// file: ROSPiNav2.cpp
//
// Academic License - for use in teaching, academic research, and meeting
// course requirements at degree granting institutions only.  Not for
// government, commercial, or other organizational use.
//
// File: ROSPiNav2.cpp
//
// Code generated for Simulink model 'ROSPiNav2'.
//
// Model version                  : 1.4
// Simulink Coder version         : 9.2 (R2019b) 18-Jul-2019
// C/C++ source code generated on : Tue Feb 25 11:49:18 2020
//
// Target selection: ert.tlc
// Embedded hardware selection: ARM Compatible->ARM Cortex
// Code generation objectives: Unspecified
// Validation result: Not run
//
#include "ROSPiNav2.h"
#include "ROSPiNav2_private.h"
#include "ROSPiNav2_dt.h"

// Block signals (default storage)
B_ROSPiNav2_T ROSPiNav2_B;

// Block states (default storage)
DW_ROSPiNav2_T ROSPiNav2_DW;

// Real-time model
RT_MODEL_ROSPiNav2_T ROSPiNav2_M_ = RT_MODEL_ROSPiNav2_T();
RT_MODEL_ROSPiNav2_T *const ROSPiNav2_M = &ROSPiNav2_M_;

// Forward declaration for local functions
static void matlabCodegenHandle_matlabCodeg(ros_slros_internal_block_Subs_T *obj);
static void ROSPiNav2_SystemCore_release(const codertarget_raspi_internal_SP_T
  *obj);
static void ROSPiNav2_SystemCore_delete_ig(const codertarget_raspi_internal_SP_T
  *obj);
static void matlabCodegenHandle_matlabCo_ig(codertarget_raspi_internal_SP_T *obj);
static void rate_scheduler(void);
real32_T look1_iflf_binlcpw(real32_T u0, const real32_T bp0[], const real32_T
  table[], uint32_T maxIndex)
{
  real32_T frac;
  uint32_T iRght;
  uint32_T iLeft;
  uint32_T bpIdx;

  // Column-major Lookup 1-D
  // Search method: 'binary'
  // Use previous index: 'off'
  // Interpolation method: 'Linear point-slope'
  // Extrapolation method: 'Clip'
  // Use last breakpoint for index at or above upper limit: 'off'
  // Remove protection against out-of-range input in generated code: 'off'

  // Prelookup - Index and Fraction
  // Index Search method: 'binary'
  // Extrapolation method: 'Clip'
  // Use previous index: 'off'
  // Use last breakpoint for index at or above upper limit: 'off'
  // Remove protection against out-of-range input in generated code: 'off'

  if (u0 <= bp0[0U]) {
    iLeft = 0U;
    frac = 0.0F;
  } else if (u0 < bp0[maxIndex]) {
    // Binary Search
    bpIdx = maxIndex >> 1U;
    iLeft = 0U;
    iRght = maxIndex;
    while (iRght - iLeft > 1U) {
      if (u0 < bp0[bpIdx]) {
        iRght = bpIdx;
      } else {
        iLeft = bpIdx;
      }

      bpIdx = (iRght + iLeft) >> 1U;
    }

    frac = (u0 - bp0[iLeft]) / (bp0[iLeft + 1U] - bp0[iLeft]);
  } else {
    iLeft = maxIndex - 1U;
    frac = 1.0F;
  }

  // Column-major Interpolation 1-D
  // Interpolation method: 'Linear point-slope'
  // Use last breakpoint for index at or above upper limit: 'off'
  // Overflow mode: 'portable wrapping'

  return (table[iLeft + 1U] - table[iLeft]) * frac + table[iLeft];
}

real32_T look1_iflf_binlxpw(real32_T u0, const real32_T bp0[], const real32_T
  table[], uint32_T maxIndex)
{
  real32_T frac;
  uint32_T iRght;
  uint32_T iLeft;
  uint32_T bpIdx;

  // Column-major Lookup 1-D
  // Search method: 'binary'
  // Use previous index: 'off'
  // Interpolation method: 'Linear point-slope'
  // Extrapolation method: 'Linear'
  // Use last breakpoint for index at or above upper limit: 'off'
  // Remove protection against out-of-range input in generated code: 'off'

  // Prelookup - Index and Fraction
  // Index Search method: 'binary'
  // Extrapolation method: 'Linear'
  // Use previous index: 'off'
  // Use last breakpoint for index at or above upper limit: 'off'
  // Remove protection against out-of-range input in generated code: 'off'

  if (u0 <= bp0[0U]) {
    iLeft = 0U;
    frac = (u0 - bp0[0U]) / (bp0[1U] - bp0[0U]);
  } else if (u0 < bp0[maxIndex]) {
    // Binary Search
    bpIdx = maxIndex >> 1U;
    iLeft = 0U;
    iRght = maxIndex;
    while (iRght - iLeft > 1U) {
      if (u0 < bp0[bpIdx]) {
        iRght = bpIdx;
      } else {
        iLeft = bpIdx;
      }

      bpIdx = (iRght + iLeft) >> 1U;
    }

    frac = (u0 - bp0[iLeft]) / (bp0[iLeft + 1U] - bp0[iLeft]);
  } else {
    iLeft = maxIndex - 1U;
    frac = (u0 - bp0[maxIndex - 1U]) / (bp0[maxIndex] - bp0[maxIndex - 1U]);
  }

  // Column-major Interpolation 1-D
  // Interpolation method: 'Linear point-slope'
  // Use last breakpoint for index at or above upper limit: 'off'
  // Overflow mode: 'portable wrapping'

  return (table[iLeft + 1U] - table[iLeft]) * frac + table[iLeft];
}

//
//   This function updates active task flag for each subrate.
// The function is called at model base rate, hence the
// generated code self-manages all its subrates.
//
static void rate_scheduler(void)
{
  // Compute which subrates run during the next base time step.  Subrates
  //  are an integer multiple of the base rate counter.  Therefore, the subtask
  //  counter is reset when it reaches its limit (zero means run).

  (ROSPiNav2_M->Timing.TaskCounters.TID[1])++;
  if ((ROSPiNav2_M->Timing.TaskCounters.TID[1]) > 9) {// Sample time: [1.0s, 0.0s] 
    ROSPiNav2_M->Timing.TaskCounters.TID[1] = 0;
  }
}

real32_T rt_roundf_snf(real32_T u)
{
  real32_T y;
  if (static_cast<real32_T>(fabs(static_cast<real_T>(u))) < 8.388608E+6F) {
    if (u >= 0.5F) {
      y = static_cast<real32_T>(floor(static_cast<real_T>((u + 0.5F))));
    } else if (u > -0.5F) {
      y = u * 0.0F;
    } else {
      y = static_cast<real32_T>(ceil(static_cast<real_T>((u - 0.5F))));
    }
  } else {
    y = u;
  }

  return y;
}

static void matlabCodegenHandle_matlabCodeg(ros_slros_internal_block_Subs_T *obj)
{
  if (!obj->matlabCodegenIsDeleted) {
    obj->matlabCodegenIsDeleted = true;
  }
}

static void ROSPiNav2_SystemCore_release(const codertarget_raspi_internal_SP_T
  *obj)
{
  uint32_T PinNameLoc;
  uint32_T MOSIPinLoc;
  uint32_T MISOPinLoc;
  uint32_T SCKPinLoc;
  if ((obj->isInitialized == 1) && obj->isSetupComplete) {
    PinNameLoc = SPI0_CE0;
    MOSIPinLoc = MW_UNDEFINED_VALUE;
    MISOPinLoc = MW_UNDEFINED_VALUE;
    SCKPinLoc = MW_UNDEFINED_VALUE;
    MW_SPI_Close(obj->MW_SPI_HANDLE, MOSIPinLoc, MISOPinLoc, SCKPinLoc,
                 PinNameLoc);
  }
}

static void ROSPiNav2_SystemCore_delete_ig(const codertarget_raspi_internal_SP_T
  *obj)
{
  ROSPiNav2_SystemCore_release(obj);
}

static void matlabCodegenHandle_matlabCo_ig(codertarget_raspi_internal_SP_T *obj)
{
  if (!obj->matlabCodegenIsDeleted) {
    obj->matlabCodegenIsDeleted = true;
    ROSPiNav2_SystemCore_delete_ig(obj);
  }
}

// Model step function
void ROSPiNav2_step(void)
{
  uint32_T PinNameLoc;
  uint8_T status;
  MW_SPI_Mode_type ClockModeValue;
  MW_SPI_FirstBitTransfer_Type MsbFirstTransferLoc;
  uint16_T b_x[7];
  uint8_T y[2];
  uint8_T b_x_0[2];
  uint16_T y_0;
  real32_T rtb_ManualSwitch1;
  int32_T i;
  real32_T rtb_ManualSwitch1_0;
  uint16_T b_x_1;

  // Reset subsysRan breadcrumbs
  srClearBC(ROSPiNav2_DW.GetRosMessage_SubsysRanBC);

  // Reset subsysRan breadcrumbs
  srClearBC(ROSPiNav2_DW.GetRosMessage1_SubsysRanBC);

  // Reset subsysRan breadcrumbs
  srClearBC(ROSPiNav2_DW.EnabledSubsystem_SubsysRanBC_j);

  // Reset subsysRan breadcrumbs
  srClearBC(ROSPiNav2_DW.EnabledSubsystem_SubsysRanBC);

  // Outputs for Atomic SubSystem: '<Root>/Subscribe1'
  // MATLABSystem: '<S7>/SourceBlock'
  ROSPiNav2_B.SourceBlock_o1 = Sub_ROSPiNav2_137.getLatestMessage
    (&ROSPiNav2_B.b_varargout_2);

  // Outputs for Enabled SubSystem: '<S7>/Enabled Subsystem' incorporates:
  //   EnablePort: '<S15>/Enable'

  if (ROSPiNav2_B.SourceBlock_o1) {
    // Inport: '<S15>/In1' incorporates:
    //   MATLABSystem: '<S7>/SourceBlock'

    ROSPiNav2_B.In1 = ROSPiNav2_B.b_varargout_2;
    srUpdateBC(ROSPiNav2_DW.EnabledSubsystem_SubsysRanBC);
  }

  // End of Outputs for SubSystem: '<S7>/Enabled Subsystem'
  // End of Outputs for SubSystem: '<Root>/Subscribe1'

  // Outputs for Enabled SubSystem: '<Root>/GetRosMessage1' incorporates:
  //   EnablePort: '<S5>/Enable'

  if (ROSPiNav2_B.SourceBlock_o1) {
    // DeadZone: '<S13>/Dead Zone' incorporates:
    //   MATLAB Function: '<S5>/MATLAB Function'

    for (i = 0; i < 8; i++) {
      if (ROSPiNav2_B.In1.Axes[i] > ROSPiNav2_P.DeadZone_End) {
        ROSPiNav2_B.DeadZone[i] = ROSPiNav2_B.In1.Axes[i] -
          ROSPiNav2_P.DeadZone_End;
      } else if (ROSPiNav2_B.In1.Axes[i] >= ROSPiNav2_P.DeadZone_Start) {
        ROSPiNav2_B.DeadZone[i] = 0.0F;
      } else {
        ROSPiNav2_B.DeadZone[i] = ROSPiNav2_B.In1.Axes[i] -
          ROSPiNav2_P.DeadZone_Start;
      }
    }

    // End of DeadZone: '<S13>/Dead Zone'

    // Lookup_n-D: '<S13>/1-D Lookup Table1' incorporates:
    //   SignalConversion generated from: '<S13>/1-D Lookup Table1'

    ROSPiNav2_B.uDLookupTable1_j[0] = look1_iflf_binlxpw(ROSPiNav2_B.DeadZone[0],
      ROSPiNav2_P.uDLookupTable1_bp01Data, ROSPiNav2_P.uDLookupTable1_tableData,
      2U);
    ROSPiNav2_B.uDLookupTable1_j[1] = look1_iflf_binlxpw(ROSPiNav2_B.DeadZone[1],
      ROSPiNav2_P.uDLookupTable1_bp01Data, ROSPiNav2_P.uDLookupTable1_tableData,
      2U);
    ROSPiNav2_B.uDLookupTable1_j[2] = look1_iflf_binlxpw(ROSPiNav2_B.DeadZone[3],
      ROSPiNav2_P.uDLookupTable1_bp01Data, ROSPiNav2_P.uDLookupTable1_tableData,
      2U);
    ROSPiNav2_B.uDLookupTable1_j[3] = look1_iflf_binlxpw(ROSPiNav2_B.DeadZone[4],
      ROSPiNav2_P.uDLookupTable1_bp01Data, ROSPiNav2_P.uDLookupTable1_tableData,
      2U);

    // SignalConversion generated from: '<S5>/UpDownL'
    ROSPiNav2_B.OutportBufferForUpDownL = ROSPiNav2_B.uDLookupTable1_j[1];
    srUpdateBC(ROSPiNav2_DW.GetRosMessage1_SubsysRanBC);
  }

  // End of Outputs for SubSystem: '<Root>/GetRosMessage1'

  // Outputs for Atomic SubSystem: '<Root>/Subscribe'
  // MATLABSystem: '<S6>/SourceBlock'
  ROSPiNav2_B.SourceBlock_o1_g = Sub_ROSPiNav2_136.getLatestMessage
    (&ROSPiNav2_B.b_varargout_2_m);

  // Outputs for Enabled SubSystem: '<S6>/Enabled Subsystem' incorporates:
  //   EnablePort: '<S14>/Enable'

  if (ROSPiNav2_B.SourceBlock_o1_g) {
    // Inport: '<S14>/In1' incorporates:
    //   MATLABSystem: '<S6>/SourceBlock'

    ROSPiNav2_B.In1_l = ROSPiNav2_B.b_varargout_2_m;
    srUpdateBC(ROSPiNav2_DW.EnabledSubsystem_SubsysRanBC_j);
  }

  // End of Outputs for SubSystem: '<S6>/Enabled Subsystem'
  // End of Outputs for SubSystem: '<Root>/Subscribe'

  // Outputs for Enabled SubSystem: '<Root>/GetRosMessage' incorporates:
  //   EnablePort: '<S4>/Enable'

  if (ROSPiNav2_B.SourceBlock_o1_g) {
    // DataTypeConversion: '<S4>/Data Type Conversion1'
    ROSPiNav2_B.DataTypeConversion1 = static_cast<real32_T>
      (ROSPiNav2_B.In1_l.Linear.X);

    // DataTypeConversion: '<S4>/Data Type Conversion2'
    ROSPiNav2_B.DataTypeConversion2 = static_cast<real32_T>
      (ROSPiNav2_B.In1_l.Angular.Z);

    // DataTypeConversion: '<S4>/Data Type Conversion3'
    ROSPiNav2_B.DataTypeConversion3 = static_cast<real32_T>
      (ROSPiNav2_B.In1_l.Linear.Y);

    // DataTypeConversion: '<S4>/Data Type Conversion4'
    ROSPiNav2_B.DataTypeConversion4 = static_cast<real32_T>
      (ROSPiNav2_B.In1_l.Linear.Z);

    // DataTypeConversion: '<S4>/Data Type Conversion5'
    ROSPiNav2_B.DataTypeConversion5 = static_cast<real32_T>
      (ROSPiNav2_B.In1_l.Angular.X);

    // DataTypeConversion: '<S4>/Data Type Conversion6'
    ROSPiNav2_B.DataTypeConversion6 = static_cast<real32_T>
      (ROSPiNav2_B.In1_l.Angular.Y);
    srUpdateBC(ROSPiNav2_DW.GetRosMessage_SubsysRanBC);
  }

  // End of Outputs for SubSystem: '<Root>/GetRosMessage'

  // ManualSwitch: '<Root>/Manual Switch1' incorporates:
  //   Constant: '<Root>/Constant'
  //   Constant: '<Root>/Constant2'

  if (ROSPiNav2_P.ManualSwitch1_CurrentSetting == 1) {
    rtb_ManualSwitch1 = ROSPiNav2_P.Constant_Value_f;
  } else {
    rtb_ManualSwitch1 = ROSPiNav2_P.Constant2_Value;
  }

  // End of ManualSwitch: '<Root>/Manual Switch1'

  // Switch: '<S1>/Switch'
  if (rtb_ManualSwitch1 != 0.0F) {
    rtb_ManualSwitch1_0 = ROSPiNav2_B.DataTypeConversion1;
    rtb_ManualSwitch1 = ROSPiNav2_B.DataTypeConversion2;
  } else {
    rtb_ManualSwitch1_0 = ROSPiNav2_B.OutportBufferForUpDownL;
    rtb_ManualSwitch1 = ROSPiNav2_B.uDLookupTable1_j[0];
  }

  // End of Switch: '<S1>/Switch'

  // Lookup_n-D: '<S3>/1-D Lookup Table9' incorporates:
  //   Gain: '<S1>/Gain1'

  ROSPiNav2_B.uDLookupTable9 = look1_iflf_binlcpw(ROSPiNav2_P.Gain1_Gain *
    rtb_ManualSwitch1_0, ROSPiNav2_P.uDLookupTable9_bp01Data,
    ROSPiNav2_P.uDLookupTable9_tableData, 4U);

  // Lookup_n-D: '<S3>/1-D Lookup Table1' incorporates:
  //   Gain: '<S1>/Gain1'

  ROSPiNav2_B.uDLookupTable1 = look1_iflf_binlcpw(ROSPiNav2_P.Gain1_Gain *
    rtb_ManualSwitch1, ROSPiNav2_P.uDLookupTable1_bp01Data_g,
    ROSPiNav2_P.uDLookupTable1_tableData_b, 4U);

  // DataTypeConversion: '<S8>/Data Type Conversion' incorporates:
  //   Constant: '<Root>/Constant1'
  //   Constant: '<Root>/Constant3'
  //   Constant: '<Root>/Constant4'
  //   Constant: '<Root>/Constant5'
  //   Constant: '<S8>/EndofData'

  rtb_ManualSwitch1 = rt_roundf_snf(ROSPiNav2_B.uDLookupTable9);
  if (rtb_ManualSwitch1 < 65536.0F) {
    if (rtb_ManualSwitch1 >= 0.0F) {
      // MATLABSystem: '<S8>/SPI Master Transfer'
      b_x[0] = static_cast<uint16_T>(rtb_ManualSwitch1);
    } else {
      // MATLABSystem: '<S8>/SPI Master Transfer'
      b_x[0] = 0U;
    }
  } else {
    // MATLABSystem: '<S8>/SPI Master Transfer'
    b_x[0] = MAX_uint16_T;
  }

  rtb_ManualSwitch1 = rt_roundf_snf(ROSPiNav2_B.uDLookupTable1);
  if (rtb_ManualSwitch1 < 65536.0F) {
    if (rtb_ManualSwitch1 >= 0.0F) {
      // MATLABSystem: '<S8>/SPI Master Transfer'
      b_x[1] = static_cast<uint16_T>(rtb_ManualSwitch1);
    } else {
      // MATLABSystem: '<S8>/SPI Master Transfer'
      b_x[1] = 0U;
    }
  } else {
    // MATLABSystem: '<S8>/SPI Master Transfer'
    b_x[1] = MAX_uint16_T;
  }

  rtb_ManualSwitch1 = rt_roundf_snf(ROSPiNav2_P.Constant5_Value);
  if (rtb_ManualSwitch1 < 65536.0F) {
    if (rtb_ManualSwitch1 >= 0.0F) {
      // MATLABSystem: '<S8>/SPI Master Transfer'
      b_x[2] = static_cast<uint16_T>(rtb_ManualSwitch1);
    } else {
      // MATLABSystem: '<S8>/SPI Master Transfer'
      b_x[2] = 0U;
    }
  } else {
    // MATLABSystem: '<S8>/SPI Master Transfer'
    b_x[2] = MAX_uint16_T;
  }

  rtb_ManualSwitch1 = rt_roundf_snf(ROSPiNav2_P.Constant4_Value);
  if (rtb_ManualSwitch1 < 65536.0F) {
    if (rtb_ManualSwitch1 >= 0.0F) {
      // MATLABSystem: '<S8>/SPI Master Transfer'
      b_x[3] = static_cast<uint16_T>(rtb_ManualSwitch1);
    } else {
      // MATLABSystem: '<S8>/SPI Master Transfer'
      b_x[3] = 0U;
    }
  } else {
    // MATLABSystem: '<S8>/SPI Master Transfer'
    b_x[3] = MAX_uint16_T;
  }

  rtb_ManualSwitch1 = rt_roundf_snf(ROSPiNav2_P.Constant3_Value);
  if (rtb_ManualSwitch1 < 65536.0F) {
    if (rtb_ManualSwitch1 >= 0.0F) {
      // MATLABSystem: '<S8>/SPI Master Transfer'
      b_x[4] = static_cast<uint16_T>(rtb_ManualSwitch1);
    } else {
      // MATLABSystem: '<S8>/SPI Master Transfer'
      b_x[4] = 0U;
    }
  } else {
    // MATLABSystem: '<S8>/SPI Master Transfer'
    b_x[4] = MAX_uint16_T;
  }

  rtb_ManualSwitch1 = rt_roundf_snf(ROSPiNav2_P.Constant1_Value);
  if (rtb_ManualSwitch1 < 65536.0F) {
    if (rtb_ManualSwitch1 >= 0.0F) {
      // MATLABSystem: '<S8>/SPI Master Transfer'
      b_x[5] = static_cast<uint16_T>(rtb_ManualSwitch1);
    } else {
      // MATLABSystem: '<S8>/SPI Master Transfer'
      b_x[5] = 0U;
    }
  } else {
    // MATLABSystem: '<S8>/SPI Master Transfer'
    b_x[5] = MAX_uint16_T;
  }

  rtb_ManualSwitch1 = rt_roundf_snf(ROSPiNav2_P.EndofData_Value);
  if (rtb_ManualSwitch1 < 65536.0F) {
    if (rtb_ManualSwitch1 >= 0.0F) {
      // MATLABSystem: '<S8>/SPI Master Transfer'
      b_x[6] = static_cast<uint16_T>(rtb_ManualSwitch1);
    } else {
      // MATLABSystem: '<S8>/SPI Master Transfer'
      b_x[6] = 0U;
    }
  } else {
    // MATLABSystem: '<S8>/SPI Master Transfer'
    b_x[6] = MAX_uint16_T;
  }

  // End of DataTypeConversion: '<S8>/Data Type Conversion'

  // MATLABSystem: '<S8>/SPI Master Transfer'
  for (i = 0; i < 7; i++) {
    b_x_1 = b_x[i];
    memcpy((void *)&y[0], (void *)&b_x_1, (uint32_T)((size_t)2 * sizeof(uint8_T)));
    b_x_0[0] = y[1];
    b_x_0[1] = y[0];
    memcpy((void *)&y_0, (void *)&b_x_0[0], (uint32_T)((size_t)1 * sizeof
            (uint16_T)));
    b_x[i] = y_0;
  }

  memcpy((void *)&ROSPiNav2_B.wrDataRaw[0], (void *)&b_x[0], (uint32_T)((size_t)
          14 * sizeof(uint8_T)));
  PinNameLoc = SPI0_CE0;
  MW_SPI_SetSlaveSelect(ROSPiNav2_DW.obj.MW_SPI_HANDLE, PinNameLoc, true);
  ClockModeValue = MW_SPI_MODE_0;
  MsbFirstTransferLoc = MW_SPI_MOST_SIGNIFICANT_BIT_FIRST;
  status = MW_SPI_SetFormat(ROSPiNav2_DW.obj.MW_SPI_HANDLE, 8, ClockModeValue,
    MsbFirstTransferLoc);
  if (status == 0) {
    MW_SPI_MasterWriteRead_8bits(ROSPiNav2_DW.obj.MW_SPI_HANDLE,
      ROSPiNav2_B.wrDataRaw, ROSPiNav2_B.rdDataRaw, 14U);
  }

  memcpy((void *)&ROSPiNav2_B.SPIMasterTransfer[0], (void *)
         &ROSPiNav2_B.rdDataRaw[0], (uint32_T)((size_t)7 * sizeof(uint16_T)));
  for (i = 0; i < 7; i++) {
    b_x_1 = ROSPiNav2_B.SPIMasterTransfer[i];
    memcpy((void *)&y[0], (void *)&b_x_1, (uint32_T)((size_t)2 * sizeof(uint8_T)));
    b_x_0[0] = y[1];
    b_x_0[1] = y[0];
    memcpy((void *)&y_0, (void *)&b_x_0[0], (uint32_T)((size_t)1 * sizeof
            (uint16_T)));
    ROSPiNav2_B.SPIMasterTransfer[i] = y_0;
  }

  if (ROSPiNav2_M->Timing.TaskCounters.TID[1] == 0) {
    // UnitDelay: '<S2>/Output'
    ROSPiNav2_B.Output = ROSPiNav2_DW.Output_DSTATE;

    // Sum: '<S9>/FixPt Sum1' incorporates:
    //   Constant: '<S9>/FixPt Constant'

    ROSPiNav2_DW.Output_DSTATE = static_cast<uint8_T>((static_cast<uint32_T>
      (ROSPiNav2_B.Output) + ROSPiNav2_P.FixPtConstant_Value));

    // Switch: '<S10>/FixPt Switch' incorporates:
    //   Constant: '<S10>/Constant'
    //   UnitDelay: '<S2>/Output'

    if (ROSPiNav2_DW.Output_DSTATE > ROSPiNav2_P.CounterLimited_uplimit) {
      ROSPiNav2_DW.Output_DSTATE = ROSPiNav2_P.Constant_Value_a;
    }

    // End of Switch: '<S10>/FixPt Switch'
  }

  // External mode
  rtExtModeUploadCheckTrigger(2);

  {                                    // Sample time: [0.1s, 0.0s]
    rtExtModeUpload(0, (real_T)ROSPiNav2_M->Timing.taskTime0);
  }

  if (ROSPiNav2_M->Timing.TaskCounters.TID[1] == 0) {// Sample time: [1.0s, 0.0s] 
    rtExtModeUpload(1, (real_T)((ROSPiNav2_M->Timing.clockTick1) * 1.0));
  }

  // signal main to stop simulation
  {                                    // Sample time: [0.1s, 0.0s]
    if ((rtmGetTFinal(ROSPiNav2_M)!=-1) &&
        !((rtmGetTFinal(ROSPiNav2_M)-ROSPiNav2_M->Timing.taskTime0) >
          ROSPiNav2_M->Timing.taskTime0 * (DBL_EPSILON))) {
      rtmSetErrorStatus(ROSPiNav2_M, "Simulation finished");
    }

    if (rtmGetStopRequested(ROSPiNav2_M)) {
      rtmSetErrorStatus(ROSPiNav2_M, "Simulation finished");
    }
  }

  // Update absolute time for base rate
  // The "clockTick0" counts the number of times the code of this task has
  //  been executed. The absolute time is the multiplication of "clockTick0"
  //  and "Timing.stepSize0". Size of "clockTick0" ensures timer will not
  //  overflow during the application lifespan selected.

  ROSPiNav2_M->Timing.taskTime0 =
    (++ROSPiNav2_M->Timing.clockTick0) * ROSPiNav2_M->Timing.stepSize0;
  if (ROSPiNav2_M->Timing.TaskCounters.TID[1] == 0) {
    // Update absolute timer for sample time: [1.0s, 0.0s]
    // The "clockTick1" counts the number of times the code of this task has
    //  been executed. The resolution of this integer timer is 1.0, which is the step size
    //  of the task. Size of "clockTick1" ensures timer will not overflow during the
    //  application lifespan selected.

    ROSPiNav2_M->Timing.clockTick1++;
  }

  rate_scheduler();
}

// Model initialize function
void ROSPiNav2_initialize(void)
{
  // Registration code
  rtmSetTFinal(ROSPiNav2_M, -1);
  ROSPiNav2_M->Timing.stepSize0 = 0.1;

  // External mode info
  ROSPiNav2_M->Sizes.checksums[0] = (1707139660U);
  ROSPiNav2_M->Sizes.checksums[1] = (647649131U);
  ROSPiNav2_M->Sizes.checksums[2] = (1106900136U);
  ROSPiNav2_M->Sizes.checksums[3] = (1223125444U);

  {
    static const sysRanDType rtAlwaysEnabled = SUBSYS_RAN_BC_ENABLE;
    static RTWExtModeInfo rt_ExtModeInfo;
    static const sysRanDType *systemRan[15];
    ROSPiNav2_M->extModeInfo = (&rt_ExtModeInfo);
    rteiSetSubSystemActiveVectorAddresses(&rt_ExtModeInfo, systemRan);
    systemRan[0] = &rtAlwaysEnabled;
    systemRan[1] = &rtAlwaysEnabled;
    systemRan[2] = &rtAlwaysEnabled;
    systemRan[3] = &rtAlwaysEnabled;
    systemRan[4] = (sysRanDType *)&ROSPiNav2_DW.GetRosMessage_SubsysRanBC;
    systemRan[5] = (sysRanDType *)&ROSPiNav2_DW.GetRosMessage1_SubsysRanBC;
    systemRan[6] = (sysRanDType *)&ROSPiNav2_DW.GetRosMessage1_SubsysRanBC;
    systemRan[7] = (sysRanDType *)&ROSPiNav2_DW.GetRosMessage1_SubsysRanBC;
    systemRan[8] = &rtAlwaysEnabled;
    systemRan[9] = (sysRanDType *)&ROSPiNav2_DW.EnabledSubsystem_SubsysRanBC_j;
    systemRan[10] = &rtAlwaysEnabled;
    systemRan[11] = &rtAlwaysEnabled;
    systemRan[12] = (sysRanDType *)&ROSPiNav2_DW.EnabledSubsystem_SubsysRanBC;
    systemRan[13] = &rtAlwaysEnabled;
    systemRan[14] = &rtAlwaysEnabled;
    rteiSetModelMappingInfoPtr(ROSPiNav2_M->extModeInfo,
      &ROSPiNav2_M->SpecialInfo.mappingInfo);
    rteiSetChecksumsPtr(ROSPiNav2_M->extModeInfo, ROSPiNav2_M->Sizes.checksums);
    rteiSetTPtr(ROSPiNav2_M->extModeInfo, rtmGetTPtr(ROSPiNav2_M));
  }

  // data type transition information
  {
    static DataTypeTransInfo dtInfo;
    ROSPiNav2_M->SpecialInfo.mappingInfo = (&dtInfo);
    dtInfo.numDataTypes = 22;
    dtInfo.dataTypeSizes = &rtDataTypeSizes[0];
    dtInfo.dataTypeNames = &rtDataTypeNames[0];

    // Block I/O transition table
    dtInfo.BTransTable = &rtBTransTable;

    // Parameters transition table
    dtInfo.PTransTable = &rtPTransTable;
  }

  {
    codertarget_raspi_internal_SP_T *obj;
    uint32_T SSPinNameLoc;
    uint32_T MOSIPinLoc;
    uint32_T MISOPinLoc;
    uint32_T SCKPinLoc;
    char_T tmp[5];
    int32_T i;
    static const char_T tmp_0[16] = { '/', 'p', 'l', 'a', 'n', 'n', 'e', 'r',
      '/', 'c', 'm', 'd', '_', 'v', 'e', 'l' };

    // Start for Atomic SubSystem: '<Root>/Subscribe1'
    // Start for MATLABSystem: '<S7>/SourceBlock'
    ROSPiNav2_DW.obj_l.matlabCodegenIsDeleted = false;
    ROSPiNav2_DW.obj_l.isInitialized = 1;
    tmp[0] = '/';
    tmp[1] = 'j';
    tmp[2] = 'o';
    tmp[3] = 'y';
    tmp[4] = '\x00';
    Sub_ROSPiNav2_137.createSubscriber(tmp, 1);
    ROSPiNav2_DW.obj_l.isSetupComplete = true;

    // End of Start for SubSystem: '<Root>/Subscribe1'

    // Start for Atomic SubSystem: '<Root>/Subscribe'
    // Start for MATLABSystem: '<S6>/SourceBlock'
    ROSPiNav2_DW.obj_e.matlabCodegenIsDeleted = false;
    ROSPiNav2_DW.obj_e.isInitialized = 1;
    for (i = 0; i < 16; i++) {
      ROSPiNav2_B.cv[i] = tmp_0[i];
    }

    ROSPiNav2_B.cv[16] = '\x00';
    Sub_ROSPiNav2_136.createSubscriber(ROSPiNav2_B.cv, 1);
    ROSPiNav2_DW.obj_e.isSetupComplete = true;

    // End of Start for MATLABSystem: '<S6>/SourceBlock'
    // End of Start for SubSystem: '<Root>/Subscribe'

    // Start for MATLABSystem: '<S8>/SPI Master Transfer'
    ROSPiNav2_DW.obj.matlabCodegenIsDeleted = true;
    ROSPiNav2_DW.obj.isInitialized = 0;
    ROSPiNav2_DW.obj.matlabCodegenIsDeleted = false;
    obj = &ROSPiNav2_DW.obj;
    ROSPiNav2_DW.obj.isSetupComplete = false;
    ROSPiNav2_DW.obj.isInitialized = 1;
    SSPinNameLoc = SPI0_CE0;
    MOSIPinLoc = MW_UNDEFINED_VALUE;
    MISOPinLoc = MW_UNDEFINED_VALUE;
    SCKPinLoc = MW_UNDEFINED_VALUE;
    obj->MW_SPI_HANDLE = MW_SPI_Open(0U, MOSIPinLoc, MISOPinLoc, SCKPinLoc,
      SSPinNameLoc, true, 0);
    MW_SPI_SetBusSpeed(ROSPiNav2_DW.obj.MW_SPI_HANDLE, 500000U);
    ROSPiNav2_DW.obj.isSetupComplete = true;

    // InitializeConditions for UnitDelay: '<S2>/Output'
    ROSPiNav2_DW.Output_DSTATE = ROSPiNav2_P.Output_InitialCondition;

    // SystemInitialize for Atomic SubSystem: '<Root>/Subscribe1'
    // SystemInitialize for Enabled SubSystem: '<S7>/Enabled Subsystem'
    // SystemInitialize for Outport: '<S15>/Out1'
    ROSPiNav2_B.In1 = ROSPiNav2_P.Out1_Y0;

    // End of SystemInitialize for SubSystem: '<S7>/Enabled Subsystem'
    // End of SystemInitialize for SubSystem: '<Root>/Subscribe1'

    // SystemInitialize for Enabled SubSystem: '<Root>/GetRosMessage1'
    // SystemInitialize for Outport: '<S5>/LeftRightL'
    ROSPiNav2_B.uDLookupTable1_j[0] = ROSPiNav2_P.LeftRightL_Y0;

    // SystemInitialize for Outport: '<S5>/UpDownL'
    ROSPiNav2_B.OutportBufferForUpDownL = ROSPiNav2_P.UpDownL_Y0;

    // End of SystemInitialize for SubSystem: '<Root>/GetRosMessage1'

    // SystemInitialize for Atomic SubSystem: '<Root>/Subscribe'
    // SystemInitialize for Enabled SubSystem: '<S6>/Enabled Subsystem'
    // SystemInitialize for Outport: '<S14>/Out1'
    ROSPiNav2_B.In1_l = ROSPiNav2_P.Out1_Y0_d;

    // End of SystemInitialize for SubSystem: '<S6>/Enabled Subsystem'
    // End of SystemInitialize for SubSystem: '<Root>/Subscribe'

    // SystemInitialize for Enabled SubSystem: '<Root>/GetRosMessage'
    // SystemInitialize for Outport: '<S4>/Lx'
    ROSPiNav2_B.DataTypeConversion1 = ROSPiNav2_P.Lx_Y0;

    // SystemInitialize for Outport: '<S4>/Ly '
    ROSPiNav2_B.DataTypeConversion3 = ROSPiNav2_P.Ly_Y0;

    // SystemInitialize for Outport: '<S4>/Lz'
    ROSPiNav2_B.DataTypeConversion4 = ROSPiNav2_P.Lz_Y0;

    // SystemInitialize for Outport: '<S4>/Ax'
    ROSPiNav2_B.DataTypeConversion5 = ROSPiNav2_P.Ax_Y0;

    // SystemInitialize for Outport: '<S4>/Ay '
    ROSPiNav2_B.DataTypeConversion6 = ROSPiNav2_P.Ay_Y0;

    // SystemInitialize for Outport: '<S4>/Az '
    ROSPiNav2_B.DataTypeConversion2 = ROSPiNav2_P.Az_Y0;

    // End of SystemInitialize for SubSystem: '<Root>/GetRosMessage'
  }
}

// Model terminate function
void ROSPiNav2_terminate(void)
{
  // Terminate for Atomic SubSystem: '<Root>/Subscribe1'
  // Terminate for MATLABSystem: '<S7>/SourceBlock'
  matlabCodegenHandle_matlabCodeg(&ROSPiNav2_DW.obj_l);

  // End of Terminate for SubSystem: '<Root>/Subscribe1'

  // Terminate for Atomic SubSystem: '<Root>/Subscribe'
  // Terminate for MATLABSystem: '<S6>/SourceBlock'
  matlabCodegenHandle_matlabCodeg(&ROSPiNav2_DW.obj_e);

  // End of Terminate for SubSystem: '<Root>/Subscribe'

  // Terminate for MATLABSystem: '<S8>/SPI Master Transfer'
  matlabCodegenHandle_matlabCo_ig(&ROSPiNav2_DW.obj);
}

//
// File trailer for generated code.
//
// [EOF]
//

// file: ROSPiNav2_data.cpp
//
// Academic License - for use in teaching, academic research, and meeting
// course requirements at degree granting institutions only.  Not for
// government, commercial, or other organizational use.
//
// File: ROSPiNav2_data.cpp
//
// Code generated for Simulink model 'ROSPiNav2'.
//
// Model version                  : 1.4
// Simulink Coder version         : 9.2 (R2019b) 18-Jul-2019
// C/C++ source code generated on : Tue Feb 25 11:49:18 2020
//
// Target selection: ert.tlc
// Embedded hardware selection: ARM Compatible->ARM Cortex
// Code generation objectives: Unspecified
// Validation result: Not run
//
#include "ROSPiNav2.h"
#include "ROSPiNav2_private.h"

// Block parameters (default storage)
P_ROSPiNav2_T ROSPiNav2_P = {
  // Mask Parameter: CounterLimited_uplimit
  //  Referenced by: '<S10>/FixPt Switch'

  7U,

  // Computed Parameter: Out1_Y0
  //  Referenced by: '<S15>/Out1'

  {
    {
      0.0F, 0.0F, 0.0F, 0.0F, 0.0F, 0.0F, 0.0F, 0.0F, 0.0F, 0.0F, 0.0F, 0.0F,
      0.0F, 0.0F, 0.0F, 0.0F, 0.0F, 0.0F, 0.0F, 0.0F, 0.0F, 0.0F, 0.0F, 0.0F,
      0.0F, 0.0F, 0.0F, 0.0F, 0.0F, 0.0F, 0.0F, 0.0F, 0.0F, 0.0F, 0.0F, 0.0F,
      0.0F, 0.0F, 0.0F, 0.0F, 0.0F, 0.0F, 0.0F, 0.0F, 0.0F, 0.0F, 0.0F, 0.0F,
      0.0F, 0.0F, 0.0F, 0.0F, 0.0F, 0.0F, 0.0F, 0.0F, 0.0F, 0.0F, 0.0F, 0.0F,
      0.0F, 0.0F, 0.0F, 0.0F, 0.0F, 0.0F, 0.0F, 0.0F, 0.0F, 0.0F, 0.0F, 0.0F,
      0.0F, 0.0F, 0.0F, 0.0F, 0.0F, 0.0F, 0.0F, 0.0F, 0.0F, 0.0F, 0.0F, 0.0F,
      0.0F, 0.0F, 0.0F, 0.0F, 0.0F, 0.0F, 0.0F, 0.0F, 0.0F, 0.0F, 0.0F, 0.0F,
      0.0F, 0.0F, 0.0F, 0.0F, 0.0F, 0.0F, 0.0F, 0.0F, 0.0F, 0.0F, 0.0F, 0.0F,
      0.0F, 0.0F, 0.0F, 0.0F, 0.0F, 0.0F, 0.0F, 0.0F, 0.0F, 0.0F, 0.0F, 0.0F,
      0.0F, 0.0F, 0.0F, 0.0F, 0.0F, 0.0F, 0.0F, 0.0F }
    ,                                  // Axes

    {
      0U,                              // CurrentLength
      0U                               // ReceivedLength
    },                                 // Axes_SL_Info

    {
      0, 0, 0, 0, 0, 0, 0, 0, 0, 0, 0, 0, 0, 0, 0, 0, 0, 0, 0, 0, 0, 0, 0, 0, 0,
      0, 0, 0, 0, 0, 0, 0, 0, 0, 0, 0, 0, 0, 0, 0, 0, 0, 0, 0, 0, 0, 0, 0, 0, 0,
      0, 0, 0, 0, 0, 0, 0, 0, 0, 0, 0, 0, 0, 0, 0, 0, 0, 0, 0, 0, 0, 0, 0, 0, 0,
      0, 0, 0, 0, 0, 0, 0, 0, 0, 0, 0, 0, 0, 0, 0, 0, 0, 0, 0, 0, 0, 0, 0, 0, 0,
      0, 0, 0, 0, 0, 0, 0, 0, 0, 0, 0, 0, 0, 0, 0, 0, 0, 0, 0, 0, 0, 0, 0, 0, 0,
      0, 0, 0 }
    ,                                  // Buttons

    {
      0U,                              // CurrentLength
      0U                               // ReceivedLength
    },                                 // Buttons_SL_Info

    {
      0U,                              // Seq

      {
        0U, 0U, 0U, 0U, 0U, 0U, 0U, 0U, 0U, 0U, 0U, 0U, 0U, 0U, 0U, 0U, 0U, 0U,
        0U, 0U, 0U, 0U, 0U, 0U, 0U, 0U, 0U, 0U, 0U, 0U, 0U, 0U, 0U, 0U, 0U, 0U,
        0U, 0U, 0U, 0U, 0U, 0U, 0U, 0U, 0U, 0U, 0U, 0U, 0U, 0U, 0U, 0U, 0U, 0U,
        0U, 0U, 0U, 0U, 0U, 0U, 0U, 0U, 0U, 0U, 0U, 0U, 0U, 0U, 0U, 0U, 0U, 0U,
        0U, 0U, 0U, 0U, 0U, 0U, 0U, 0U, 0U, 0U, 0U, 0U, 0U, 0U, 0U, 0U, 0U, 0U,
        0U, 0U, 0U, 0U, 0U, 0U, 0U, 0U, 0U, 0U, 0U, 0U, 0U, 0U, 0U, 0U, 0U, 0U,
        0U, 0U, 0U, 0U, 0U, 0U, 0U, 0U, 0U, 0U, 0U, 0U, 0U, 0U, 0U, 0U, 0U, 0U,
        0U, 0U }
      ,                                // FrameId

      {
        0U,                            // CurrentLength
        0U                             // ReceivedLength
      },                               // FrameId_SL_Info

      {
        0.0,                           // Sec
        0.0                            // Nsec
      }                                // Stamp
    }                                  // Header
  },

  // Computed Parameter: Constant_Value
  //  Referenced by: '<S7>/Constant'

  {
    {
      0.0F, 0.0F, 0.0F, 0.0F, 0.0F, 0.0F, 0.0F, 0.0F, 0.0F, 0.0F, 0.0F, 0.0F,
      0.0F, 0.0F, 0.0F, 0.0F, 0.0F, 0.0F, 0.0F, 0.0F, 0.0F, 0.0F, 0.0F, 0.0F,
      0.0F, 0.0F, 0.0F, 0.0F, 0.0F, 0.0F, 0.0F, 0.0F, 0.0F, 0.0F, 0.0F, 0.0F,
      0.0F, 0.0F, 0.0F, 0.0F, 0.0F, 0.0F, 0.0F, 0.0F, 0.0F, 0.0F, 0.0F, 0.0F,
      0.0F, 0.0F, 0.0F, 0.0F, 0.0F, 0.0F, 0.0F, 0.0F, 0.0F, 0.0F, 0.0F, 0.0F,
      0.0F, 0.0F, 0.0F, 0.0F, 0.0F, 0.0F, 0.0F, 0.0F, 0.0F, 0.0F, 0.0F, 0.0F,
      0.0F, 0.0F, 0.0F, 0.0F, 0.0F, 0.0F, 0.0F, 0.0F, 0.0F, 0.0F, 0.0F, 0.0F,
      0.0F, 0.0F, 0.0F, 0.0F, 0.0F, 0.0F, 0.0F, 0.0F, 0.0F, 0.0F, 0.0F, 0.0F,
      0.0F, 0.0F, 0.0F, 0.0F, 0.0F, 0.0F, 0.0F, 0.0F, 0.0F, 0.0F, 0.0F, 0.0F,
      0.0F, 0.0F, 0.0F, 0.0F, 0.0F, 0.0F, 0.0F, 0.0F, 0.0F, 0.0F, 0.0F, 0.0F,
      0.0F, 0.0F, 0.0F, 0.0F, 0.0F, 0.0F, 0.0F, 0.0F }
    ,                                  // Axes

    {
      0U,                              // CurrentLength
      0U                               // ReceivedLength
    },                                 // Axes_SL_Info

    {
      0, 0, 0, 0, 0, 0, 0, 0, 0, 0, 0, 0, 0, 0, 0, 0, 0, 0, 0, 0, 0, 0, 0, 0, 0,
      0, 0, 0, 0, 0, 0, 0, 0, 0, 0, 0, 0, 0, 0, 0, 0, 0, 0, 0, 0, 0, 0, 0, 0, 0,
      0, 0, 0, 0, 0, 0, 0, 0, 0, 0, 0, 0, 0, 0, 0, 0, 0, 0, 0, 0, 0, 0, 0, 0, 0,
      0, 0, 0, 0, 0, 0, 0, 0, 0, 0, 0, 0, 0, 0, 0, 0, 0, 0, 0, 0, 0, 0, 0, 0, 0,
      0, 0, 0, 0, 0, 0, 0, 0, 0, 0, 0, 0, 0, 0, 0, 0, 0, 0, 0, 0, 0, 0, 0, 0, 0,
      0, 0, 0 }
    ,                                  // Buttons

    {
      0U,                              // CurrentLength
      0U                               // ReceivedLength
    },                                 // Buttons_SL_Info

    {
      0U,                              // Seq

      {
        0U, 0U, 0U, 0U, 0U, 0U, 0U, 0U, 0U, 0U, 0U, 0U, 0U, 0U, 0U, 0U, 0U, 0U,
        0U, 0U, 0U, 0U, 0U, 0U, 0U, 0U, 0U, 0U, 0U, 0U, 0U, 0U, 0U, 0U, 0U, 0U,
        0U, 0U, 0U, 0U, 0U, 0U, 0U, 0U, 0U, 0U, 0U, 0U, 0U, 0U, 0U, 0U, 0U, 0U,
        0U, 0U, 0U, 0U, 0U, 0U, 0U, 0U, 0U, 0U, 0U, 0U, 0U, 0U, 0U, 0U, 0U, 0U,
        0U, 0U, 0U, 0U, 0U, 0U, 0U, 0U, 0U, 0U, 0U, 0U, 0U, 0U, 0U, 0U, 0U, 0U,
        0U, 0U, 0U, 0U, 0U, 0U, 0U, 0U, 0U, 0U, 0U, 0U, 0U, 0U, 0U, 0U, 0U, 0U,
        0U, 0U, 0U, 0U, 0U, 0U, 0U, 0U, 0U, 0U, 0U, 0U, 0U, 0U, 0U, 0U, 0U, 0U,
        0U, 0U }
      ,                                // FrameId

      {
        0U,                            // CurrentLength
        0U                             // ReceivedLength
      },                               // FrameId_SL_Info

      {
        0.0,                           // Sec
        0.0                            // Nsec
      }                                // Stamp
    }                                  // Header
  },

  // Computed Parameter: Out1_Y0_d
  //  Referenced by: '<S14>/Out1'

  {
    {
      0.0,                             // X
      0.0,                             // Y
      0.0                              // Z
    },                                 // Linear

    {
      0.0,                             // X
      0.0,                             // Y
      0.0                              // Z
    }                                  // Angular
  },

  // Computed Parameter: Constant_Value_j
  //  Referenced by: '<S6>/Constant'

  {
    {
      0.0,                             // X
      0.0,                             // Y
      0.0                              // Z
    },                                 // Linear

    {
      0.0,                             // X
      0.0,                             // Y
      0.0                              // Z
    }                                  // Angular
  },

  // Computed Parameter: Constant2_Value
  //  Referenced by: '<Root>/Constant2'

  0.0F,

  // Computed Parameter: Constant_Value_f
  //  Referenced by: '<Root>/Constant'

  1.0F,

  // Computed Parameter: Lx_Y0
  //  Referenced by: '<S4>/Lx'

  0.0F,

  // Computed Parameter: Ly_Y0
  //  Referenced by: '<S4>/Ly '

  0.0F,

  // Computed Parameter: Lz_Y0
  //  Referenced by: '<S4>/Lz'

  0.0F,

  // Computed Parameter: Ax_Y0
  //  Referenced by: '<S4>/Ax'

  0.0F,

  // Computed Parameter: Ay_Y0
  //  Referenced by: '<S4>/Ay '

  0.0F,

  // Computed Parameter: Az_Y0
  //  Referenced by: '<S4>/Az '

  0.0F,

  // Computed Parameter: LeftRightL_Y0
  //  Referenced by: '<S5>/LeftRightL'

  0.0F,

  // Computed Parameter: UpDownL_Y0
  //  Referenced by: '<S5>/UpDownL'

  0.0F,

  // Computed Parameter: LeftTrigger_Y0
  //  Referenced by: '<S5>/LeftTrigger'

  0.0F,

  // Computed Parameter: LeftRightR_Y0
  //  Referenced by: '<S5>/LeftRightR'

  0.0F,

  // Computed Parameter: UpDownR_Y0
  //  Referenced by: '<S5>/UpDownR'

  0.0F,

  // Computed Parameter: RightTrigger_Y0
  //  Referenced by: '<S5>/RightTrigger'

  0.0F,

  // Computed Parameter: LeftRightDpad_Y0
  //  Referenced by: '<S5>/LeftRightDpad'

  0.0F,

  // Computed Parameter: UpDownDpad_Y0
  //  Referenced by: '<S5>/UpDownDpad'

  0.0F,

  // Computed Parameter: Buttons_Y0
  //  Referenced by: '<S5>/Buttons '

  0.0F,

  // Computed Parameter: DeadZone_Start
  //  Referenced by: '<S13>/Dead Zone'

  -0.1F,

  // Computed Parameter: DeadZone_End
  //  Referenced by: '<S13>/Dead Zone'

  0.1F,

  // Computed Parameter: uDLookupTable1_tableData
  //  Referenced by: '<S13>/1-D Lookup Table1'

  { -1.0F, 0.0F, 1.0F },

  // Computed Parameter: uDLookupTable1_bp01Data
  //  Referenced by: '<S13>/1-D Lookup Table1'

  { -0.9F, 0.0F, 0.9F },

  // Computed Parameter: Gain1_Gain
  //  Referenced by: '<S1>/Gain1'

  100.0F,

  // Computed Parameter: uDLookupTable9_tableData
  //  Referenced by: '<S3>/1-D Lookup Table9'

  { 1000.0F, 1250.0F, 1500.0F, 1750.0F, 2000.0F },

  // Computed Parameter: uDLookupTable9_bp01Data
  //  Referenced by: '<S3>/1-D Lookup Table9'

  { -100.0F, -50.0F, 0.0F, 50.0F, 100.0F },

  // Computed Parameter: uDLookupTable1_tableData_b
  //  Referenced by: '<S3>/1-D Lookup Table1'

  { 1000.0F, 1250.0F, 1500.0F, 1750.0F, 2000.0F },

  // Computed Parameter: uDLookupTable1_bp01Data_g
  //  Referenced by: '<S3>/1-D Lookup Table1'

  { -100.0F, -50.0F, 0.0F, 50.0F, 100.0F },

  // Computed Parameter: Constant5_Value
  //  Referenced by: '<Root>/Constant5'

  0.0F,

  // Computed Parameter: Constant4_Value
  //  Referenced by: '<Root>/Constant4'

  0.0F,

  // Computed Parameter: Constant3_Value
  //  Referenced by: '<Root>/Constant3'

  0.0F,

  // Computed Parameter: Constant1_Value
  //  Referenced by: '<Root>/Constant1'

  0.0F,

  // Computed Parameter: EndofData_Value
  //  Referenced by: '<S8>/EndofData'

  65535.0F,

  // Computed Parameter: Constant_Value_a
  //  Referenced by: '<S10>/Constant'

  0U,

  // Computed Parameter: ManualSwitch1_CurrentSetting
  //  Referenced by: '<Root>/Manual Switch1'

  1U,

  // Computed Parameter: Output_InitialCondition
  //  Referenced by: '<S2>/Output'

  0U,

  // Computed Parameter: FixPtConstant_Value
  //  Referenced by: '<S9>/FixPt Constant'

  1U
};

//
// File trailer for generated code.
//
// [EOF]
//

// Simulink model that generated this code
simulink model "ROSPiNav2"  (Simulink 10.0)
settings: Solver=FixedStepAuto  StartTime=0.0  StopTime=inf  RelTol=1e-3
libraries: sensehatlib x5, robotlib x2, simulink x1, raspberrypilib x1

== system ROSPiNav2 ==
  note: Arbitration
  note: Xbox Controller
  note: Raspbery Pi Sense Hat
  note: Switch Xbox or AutoNav
  note: Cheeky Dev Interface
  note: Xbox
  note: Counter to show Pi is functiuoning when running in external mode
  note: Send Data
  note: Navigation Stack
  note: Mapping
  note: AutoNav
  Arbitration : Subsystem
  Constant : Constant  OutDataTypeStr=single
  Constant{1..5} (5 alike) : Constant  Value=0  OutDataTypeStr=single
  Constant6 : Constant  Commented=on  Value=0  OutDataTypeStr=single
  Constant7 : Constant  Commented=on  Value=0  OutDataTypeStr=single
  Counter Limited : simulink/Sources/Counter Limited  uplimit=7  tsamp=1
  Display{1..6,15} (7 alike) : Display
  ForwardBack_LeftRight : Subsystem
  From2 : From  Commented=on  GotoTag=SenseHatOut
  GetRosMessage : Subsystem
  GetRosMessage1 : Subsystem
  Goto2 : Goto  Commented=on  GotoTag=SenseHatOut
  Manual Switch1 : ManualSwitch
  Mux : Mux  Commented=on  Inputs=7
  Mux1 : Mux  Inputs=2
  Mux2 : Mux  Inputs=6
  Mux3 : Mux  Inputs=2
  PiSenseHat : Subsystem  Commented=on
  SPI Return : Display
  Subscribe : robotlib/Subscribe  topicSource=Select from ROS network  topic=/planner/cmd_vel  messageType=geometry_msgs/Twist  sampleTime=0.1  messageQueueLength=1
  Subscribe1 : robotlib/Subscribe  topicSource=Specify your own  topic=/joy  messageType=sensor_msgs/Joy  sampleTime=0.1  messageQueueLength=1
  Subsystem : Subsystem
  Terminator{1..11} (11 alike) : Terminator
  wires:
  GetRosMessage1/2(UpDownL) -> Mux1/2, Arbitration/3("ControllerUpDown ")
  [SPIOutput] -> SPI Return/1
  Mux3/1 -> [DataSent]
  [DataSent] -> Display6/1
  [InputCmd] -> Arbitration/5("Switch ")
  GetRosMessage1/9("Buttons ") -> Terminator11/1
  Constant5/1 -> Subsystem/3(Spare1)
  GetRosMessage1/7(LeftRightDpad) -> Terminator9/1
  Constant4/1 -> Subsystem/4(Spare2)
  Constant/1 -> Manual Switch1/1
  ForwardBack_LeftRight/1(ForwardsBack) -> Mux3/1, Subsystem/1(ForwardsBackwards)
  ForwardBack_LeftRight/2(LeftRight) -> Mux3/2, Subsystem/2(LeftRight)
  GetRosMessage1/5(UpDownR) -> Terminator7/1
  Arbitration/1(ForwardBackOut) -> ForwardBack_LeftRight/1(In1)
  Subscribe/2 -> GetRosMessage/1(In1)
  GetRosMessage/5("Ay ") -> Mux2/5, Terminator5/1
  GetRosMessage/3(Lz) -> Mux2/3, Terminator3/1
  Constant2/1 -> Manual Switch1/2
  GetRosMessage/4(Ax) -> Mux2/4, Terminator4/1
  GetRosMessage1/4(LeftRightR) -> Terminator6/1
  PiSenseHat/1(PressureP) -> Mux/1
  From2/1 -> Display3/1
  Subscribe/1 -> GetRosMessage/Enable, Display1/1
  GetRosMessage/2("Ly ") -> Mux2/2, Terminator2/1
  Subscribe1/2 -> GetRosMessage1/1(In1)
  [XboxOut] -> Display5/1
  PiSenseHat/7(HumidityT) -> Mux/7
  Constant3/1 -> Subsystem/5(Spare3)
  GetRosMessage1/8(UpDownDpad) -> Terminator10/1
  Mux2/1 -> [NavStackOut]
  Subscribe1/1 -> GetRosMessage1/Enable, Display2/1
  GetRosMessage/6("Az ") -> Arbitration/2(LeftyRightyIn), Mux2/6  "Left_right"
  PiSenseHat/5(MagField) -> Mux/5
  Subsystem/1(SpiData) -> [SPIOutput]
  Constant1/1 -> Subsystem/6(Spare4)
  Mux1/1 -> [XboxOut]
  PiSenseHat/4(Accel) -> Mux/4
  Counter Limited/1 -> Display15/1
  GetRosMessage1/1(LeftRightL) -> Mux1/1, Arbitration/4(ControllerLeftRight)
  GetRosMessage1/3(LeftTrigger) -> Terminator1/1
  GetRosMessage1/6(RightTrigger) -> Terminator8/1
  Arbitration/2(LeftyRightyOut) -> ForwardBack_LeftRight/2(In2)
  GetRosMessage/1(Lx) -> Mux2/1, Arbitration/1(ForwardBackIn)  "Forward_Back"
  [NavStackOut] -> Display4/1
  Manual Switch1/1 -> [InputCmd]
  PiSenseHat/3(AngVelocity) -> Mux/3
  Mux/1 -> Goto2/1
  PiSenseHat/6(HumidityH) -> Mux/6
  PiSenseHat/2(PressureT) -> Mux/2

== system ROSPiNav2/Arbitration ==
  note: Possibility here to switch from the commands to a fixed velocity
  note: Looking here to see if we are on the stright and narrow if not, pause and rotate before moving forwards.
      | The data coming from the Navigation node gives forward velocity and twist velocity. this ranges from -0.5 to 0.5 on both sides.
  ForwardBackIn : Inport
  LeftyRightyIn : Inport  Port=2
  "ControllerUpDown " : Inport  Port=3
  ControllerLeftRight : Inport  Port=4
  "Switch " : Inport  Port=5
  Demux : Demux  Outputs=2
  Gain1 : Gain  Gain=100
  Mux1 : Mux  Inputs=2
  Mux2 : Mux  Inputs=2
  Switch : Switch  Criteria=u2 ~= 0
  ForwardBackOut : Outport
  LeftyRightyOut : Outport  Port=2
  wires:
  LeftyRightyIn/1 -> Mux2/2
  Demux/1 -> ForwardBackOut/1
  Demux/2 -> LeftyRightyOut/1
  Switch/1 -> Gain1/1
  "ControllerUpDown "/1 -> Mux1/1
  ControllerLeftRight/1 -> Mux1/2
  Mux1/1 -> Switch/3
  "Switch "/1 -> Switch/2
  Gain1/1 -> Demux/1
  Mux2/1 -> Switch/1
  ForwardBackIn/1 -> Mux2/1

== system ROSPiNav2/ForwardBack_LeftRight ==
  note: input a -100 to 100 value for reverse and forwards. -100 is 100% speed backwards 100 is 100%speed forwards
  note: input a -100 to 100 value for left and right. -100 is 100% speed left 100 is 100%speed right
  In1 : Inport
  In2 : Inport  Port=2
  1-D Lookup Table1 : Lookup_n-D  NumberOfTableDimensions=1  BreakpointsForDimension1=[-100,-50,0,50,100]  BreakpointsForDimension1FirstPoint=0  BreakpointsForDimension1Spacing=1.8  Table=[1000;1250;1500;1750;2000;]  ExtrapMethod=Clip  InternalRulePriority=Speed  OutDataTypeStr=single  RndMeth=Simplest  InputSameDT=on
  1-D Lookup Table9 : Lookup_n-D  NumberOfTableDimensions=1  BreakpointsForDimension1=[-100,-50,0,50,100]  BreakpointsForDimension1FirstPoint=0  BreakpointsForDimension1Spacing=1.8  Table=[1000;1250;1500;1750;2000]  ExtrapMethod=Clip  InternalRulePriority=Speed  OutDataTypeStr=single  RndMeth=Simplest  InputSameDT=on
  ForwardsBack : Outport  OutDataTypeStr=single
  LeftRight : Outport  Port=2  OutDataTypeStr=single
  wires:
  In1/1 -> 1-D Lookup Table9/1
  1-D Lookup Table1/1 -> LeftRight/1
  1-D Lookup Table9/1 -> ForwardsBack/1
  In2/1 -> 1-D Lookup Table1/1

== system ROSPiNav2/GetRosMessage ==
  note: Linear Commands
  note: AngularCommands
  In1 : Inport
  Enable : EnablePort
  Bus Selector : BusSelector  OutputSignals=Linear.X,Linear.Y,Linear.Z,Angular.X,Angular.Y,Angular.Z
  Data Type Conversion{1..6} (6 alike) : DataTypeConversion  OutDataTypeStr=single
  Lx : Outport  OutDataTypeStr=single
  "Ly " : Outport  Port=2
  Lz : Outport  Port=3
  Ax : Outport  Port=4
  "Ay " : Outport  Port=5
  "Az " : Outport  Port=6  OutDataTypeStr=single
  wires:
  Bus Selector/2 -> Data Type Conversion3/1  "<Y>"
  Bus Selector/1 -> Data Type Conversion1/1  "<X>"
  In1/1 -> Bus Selector/1
  Bus Selector/3 -> Data Type Conversion4/1  "<Z>"
  Bus Selector/4 -> Data Type Conversion5/1  "<X>"
  Bus Selector/5 -> Data Type Conversion6/1  "<Y>"
  Bus Selector/6 -> Data Type Conversion2/1  "<Z>"
  Data Type Conversion1/1 -> Lx/1
  Data Type Conversion2/1 -> "Az "/1
  Data Type Conversion3/1 -> "Ly "/1
  Data Type Conversion4/1 -> Lz/1
  Data Type Conversion5/1 -> Ax/1
  Data Type Conversion6/1 -> "Ay "/1

== system ROSPiNav2/GetRosMessage1 ==
  note: Axes
  In1 : Inport
  Enable : EnablePort
  Bus Selector : BusSelector  OutputSignals=Axes,Buttons
  Data Type Conversion1 : DataTypeConversion  OutDataTypeStr=single
  Data Type Conversion3 : DataTypeConversion  OutDataTypeStr=single
  Demux : Demux  Outputs=8
  MATLAB Function : MATLAB Function  TreatAsAtomicUnit=on
  MATLAB Function1 : MATLAB Function  TreatAsAtomicUnit=on
  "XboxControllerMappings " : Subsystem
  LeftRightL : Outport  OutDataTypeStr=single
  UpDownL : Outport  Port=2  OutDataTypeStr=single
  LeftTrigger : Outport  Port=3  OutDataTypeStr=single
  LeftRightR : Outport  Port=4  OutDataTypeStr=single
  UpDownR : Outport  Port=5  OutDataTypeStr=single
  RightTrigger : Outport  Port=6  OutDataTypeStr=single
  LeftRightDpad : Outport  Port=7  OutDataTypeStr=single
  UpDownDpad : Outport  Port=8  OutDataTypeStr=single
  "Buttons " : Outport  Port=9
  wires:
  Data Type Conversion3/1 -> "Buttons "/1
  Demux/1 -> LeftRightL/1
  In1/1 -> Bus Selector/1
  Bus Selector/1 -> MATLAB Function/1(in)  "<Axes>"
  Bus Selector/2 -> MATLAB Function1/1(in)  "<Buttons>"
  Data Type Conversion1/1 -> "XboxControllerMappings "/1(Axisin)
  Demux/2 -> UpDownL/1
  Demux/3 -> LeftTrigger/1
  Demux/4 -> LeftRightR/1
  Demux/5 -> UpDownR/1
  Demux/6 -> RightTrigger/1
  Demux/7 -> LeftRightDpad/1
  "XboxControllerMappings "/1(AxisOut) -> Demux/1
  Demux/8 -> UpDownDpad/1
  MATLAB Function/1(out) -> Data Type Conversion1/1
  MATLAB Function1/1(out) -> Data Type Conversion3/1

== system ROSPiNav2/PiSenseHat ==
  note: For some reason the GPIO is broken. I don't know why. but these two blocks do not work. However the IMU data we care about is fine
  "8x8 RGB LED Matrix " : sensehatlib/8x8 RGB LED Matrix   Commented=on  Mode=Write Pixel  ImageSource=One multidimensional signal  OrientationSource=Block dialog  LEDOrientation=0  blockPlatform=Raspberry pi
  Display3 : Display
  HTS221 Humidity Sensor : sensehatlib/HTS221 Humidity Sensor  BoardProperty=Pi 2 Model B  OutputDataRate=12.5 Hz  SampleTime=0.1
  Joystick : sensehatlib/Joystick  Commented=on  SampleTime=0.5  blockPlatform=Raspberry Pi
  LPS25H Pressure Sensor : sensehatlib/LPS25H Pressure Sensor  BoardProperty=Pi 3 Model B+  OutputDataRate=12.5 Hz  SampleTime=0.2
  LSM9DS1 IMU Sensor : sensehatlib/LSM9DS1 IMU Sensor  blockPlatform=Raspberry Pi  BoardProperty_sh=Pi 3 Model B  ActiveSensors_=Accelerometer, Gyroscope and Magnetometer  AccelerometerOutputDataRate=119 Hz  AccelerometerFullScaleRange=+/- 2g  AccelerometerBandwidth=50 Hz  GyroscopeOutputDataRate=119 Hz  GyroscopeFullScaleRange=245 dps  GyroscopeBandwidthMode=0  GyroscopeHighPassFilterEnabled=off  GyroscopeHighPassFilterMode=0  MagnetometerFullScaleRange=+/- 4 gauss  MagnetometerOutputDataRate=40 Hz  SampleTime=0.1
  MATLAB Function : MATLAB Function  TreatAsAtomicUnit=on
  MATLAB Function1 : MATLAB Function  TreatAsAtomicUnit=on
  MATLAB Function2 : MATLAB Function  TreatAsAtomicUnit=on
  PressureP : Outport
  PressureT : Outport  Port=2
  AngVelocity : Outport  Port=3
  Accel : Outport  Port=4
  MagField : Outport  Port=5
  HumidityH : Outport  Port=6
  HumidityT : Outport  Port=7
  wires:
  HTS221 Humidity Sensor/2 -> HumidityT/1
  HTS221 Humidity Sensor/1 -> HumidityH/1
  Joystick/1 -> Display3/1
  LSM9DS1 IMU Sensor/1 -> MATLAB Function/1(angvel), MATLAB Function2/1(a)
  LPS25H Pressure Sensor/1 -> PressureP/1
  LPS25H Pressure Sensor/2 -> PressureT/1
  LSM9DS1 IMU Sensor/2 -> MATLAB Function/2(accel), MATLAB Function1/1(a)
  MATLAB Function/1(orientation2) -> MagField/1
  MATLAB Function1/1(out) -> Accel/1
  MATLAB Function2/1(out) -> AngVelocity/1
  LSM9DS1 IMU Sensor/3 -> MATLAB Function/3(magdata)

== system ROSPiNav2/Subsystem ==
  ForwardsBackwards : Inport
  LeftRight : Inport  Port=2
  Spare1 : Inport  Port=3
  Spare2 : Inport  Port=4
  Spare3 : Inport  Port=5
  Spare4 : Inport  Port=6
  Data Type Conversion : DataTypeConversion  OutDataTypeStr=uint16  RndMeth=Round  SaturateOnIntegerOverflow=on
  EndofData : Constant  Value=65535  OutDataTypeStr=single
  Mux : Mux  Inputs=7
  Rate Transition1 : RateTransition  OutPortSampleTime=0.1
  SPI Master Transfer : raspberrypilib/SPI Master Transfer  BoardProperty=Pi 3 Model B+  SPIModule=uint32(0)  Mode=Master  BusSpeed=1000000  Pin=SPI0_CE0  FirstBitToTransfer=Most significant bit (MSB)  ClockMode=0  BlockFunction=Transfer  RegisterAddress=0  OutputDataType=int8  OutputDataLength=1
  SpiData : Outport
  wires:
  LeftRight/1 -> Mux/2
  ForwardsBackwards/1 -> Mux/1
  Spare4/1 -> Mux/6
  Mux/1 -> Data Type Conversion/1
  EndofData/1 -> Mux/7
  Rate Transition1/1 -> SPI Master Transfer/1
  Data Type Conversion/1 -> Rate Transition1/1
  Spare2/1 -> Mux/4
  Spare3/1 -> Mux/5
  SPI Master Transfer/1 -> SpiData/1
  Spare1/1 -> Mux/3

== system ROSPiNav2/GetRosMessage1/XboxControllerMappings  ==
  note: add a dead zone
  note: D PAD
  Axisin : Inport
  1-D Lookup Table1 : Lookup_n-D  NumberOfTableDimensions=1  BreakpointsForDimension1=[-0.9,0,0.9]  Table=[-1,0,1]  InternalRulePriority=Speed  RndMeth=Simplest  InputSameDT=on
  Dead Zone : DeadZone  LowerValue=-0.1  UpperValue=0.1  SaturateOnIntegerOverflow=on
  Demux1 : Demux  Outputs=8
  Demux2 : Demux  Outputs=2
  Demux3 : Demux
  Mux : Mux  Inputs=8
  Mux2 : Mux  Inputs=2
  Mux3 : Mux
  Triggers : Lookup_n-D  NumberOfTableDimensions=1  BreakpointsForDimension1=[-0.9,0,0.9]  Table=[0,0.5,1]  InternalRulePriority=Speed  RndMeth=Simplest  InputSameDT=on
  AxisOut : Outport
  wires:
  Demux1/2 -> Mux3/2
  Demux1/3 -> Mux2/1
  Demux1/1 -> Mux3/1
  Demux1/7 -> Mux/7
  Axisin/1 -> Dead Zone/1
  Demux1/5 -> Mux3/4
  Demux1/6 -> Mux2/2
  Demux1/8 -> Mux/8
  Mux3/1 -> 1-D Lookup Table1/1
  Dead Zone/1 -> Demux1/1
  Demux1/4 -> Mux3/3
  Triggers/1 -> Demux2/1
  Mux2/1 -> Triggers/1
  Mux/1 -> AxisOut/1
  1-D Lookup Table1/1 -> Demux3/1
  Demux2/2 -> Mux/6
  Demux2/1 -> Mux/3
  Demux3/1 -> Mux/1
  Demux3/2 -> Mux/2
  Demux3/3 -> Mux/4
  Demux3/4 -> Mux/5

== matlab function GetRosMessage1/MATLAB Function1 ==
function out = fcn(in)

out = in(1:7);

== matlab function GetRosMessage1/MATLAB Function ==
function out = fcn(in)

out = in(1:8);

== matlab function PiSenseHat/MATLAB Function ==
function orientation2 = fcn(angvel, accel, magdata)

% x = a(:,1);
% y = a(:,2);
% z = a(:,3);
decim = 1;
FUSE = ahrsfilter('DecimationFactor',decim);
% out = atan(y/x) * (180/pi);
% orientation = 0;
[orientation] = FUSE(accel,angvel,magdata);
orientation = eulerd(orientation,'ZYX','frame');
orientation2 = orientation(1,3);

== matlab function PiSenseHat/MATLAB Function1 ==
function out = fcn(a)
x = a(:,1);
y = a(:,2);
z = a(:,3);
out = sqrt(sum(x.^2 + y.^2 + z.^2, 2));

== matlab function PiSenseHat/MATLAB Function2 ==
function out = fcn(a)
x = a(:,1);
y = a(:,2);
z = a(:,3);
out = sqrt(sum(x.^2 + y.^2 + z.^2, 2));
